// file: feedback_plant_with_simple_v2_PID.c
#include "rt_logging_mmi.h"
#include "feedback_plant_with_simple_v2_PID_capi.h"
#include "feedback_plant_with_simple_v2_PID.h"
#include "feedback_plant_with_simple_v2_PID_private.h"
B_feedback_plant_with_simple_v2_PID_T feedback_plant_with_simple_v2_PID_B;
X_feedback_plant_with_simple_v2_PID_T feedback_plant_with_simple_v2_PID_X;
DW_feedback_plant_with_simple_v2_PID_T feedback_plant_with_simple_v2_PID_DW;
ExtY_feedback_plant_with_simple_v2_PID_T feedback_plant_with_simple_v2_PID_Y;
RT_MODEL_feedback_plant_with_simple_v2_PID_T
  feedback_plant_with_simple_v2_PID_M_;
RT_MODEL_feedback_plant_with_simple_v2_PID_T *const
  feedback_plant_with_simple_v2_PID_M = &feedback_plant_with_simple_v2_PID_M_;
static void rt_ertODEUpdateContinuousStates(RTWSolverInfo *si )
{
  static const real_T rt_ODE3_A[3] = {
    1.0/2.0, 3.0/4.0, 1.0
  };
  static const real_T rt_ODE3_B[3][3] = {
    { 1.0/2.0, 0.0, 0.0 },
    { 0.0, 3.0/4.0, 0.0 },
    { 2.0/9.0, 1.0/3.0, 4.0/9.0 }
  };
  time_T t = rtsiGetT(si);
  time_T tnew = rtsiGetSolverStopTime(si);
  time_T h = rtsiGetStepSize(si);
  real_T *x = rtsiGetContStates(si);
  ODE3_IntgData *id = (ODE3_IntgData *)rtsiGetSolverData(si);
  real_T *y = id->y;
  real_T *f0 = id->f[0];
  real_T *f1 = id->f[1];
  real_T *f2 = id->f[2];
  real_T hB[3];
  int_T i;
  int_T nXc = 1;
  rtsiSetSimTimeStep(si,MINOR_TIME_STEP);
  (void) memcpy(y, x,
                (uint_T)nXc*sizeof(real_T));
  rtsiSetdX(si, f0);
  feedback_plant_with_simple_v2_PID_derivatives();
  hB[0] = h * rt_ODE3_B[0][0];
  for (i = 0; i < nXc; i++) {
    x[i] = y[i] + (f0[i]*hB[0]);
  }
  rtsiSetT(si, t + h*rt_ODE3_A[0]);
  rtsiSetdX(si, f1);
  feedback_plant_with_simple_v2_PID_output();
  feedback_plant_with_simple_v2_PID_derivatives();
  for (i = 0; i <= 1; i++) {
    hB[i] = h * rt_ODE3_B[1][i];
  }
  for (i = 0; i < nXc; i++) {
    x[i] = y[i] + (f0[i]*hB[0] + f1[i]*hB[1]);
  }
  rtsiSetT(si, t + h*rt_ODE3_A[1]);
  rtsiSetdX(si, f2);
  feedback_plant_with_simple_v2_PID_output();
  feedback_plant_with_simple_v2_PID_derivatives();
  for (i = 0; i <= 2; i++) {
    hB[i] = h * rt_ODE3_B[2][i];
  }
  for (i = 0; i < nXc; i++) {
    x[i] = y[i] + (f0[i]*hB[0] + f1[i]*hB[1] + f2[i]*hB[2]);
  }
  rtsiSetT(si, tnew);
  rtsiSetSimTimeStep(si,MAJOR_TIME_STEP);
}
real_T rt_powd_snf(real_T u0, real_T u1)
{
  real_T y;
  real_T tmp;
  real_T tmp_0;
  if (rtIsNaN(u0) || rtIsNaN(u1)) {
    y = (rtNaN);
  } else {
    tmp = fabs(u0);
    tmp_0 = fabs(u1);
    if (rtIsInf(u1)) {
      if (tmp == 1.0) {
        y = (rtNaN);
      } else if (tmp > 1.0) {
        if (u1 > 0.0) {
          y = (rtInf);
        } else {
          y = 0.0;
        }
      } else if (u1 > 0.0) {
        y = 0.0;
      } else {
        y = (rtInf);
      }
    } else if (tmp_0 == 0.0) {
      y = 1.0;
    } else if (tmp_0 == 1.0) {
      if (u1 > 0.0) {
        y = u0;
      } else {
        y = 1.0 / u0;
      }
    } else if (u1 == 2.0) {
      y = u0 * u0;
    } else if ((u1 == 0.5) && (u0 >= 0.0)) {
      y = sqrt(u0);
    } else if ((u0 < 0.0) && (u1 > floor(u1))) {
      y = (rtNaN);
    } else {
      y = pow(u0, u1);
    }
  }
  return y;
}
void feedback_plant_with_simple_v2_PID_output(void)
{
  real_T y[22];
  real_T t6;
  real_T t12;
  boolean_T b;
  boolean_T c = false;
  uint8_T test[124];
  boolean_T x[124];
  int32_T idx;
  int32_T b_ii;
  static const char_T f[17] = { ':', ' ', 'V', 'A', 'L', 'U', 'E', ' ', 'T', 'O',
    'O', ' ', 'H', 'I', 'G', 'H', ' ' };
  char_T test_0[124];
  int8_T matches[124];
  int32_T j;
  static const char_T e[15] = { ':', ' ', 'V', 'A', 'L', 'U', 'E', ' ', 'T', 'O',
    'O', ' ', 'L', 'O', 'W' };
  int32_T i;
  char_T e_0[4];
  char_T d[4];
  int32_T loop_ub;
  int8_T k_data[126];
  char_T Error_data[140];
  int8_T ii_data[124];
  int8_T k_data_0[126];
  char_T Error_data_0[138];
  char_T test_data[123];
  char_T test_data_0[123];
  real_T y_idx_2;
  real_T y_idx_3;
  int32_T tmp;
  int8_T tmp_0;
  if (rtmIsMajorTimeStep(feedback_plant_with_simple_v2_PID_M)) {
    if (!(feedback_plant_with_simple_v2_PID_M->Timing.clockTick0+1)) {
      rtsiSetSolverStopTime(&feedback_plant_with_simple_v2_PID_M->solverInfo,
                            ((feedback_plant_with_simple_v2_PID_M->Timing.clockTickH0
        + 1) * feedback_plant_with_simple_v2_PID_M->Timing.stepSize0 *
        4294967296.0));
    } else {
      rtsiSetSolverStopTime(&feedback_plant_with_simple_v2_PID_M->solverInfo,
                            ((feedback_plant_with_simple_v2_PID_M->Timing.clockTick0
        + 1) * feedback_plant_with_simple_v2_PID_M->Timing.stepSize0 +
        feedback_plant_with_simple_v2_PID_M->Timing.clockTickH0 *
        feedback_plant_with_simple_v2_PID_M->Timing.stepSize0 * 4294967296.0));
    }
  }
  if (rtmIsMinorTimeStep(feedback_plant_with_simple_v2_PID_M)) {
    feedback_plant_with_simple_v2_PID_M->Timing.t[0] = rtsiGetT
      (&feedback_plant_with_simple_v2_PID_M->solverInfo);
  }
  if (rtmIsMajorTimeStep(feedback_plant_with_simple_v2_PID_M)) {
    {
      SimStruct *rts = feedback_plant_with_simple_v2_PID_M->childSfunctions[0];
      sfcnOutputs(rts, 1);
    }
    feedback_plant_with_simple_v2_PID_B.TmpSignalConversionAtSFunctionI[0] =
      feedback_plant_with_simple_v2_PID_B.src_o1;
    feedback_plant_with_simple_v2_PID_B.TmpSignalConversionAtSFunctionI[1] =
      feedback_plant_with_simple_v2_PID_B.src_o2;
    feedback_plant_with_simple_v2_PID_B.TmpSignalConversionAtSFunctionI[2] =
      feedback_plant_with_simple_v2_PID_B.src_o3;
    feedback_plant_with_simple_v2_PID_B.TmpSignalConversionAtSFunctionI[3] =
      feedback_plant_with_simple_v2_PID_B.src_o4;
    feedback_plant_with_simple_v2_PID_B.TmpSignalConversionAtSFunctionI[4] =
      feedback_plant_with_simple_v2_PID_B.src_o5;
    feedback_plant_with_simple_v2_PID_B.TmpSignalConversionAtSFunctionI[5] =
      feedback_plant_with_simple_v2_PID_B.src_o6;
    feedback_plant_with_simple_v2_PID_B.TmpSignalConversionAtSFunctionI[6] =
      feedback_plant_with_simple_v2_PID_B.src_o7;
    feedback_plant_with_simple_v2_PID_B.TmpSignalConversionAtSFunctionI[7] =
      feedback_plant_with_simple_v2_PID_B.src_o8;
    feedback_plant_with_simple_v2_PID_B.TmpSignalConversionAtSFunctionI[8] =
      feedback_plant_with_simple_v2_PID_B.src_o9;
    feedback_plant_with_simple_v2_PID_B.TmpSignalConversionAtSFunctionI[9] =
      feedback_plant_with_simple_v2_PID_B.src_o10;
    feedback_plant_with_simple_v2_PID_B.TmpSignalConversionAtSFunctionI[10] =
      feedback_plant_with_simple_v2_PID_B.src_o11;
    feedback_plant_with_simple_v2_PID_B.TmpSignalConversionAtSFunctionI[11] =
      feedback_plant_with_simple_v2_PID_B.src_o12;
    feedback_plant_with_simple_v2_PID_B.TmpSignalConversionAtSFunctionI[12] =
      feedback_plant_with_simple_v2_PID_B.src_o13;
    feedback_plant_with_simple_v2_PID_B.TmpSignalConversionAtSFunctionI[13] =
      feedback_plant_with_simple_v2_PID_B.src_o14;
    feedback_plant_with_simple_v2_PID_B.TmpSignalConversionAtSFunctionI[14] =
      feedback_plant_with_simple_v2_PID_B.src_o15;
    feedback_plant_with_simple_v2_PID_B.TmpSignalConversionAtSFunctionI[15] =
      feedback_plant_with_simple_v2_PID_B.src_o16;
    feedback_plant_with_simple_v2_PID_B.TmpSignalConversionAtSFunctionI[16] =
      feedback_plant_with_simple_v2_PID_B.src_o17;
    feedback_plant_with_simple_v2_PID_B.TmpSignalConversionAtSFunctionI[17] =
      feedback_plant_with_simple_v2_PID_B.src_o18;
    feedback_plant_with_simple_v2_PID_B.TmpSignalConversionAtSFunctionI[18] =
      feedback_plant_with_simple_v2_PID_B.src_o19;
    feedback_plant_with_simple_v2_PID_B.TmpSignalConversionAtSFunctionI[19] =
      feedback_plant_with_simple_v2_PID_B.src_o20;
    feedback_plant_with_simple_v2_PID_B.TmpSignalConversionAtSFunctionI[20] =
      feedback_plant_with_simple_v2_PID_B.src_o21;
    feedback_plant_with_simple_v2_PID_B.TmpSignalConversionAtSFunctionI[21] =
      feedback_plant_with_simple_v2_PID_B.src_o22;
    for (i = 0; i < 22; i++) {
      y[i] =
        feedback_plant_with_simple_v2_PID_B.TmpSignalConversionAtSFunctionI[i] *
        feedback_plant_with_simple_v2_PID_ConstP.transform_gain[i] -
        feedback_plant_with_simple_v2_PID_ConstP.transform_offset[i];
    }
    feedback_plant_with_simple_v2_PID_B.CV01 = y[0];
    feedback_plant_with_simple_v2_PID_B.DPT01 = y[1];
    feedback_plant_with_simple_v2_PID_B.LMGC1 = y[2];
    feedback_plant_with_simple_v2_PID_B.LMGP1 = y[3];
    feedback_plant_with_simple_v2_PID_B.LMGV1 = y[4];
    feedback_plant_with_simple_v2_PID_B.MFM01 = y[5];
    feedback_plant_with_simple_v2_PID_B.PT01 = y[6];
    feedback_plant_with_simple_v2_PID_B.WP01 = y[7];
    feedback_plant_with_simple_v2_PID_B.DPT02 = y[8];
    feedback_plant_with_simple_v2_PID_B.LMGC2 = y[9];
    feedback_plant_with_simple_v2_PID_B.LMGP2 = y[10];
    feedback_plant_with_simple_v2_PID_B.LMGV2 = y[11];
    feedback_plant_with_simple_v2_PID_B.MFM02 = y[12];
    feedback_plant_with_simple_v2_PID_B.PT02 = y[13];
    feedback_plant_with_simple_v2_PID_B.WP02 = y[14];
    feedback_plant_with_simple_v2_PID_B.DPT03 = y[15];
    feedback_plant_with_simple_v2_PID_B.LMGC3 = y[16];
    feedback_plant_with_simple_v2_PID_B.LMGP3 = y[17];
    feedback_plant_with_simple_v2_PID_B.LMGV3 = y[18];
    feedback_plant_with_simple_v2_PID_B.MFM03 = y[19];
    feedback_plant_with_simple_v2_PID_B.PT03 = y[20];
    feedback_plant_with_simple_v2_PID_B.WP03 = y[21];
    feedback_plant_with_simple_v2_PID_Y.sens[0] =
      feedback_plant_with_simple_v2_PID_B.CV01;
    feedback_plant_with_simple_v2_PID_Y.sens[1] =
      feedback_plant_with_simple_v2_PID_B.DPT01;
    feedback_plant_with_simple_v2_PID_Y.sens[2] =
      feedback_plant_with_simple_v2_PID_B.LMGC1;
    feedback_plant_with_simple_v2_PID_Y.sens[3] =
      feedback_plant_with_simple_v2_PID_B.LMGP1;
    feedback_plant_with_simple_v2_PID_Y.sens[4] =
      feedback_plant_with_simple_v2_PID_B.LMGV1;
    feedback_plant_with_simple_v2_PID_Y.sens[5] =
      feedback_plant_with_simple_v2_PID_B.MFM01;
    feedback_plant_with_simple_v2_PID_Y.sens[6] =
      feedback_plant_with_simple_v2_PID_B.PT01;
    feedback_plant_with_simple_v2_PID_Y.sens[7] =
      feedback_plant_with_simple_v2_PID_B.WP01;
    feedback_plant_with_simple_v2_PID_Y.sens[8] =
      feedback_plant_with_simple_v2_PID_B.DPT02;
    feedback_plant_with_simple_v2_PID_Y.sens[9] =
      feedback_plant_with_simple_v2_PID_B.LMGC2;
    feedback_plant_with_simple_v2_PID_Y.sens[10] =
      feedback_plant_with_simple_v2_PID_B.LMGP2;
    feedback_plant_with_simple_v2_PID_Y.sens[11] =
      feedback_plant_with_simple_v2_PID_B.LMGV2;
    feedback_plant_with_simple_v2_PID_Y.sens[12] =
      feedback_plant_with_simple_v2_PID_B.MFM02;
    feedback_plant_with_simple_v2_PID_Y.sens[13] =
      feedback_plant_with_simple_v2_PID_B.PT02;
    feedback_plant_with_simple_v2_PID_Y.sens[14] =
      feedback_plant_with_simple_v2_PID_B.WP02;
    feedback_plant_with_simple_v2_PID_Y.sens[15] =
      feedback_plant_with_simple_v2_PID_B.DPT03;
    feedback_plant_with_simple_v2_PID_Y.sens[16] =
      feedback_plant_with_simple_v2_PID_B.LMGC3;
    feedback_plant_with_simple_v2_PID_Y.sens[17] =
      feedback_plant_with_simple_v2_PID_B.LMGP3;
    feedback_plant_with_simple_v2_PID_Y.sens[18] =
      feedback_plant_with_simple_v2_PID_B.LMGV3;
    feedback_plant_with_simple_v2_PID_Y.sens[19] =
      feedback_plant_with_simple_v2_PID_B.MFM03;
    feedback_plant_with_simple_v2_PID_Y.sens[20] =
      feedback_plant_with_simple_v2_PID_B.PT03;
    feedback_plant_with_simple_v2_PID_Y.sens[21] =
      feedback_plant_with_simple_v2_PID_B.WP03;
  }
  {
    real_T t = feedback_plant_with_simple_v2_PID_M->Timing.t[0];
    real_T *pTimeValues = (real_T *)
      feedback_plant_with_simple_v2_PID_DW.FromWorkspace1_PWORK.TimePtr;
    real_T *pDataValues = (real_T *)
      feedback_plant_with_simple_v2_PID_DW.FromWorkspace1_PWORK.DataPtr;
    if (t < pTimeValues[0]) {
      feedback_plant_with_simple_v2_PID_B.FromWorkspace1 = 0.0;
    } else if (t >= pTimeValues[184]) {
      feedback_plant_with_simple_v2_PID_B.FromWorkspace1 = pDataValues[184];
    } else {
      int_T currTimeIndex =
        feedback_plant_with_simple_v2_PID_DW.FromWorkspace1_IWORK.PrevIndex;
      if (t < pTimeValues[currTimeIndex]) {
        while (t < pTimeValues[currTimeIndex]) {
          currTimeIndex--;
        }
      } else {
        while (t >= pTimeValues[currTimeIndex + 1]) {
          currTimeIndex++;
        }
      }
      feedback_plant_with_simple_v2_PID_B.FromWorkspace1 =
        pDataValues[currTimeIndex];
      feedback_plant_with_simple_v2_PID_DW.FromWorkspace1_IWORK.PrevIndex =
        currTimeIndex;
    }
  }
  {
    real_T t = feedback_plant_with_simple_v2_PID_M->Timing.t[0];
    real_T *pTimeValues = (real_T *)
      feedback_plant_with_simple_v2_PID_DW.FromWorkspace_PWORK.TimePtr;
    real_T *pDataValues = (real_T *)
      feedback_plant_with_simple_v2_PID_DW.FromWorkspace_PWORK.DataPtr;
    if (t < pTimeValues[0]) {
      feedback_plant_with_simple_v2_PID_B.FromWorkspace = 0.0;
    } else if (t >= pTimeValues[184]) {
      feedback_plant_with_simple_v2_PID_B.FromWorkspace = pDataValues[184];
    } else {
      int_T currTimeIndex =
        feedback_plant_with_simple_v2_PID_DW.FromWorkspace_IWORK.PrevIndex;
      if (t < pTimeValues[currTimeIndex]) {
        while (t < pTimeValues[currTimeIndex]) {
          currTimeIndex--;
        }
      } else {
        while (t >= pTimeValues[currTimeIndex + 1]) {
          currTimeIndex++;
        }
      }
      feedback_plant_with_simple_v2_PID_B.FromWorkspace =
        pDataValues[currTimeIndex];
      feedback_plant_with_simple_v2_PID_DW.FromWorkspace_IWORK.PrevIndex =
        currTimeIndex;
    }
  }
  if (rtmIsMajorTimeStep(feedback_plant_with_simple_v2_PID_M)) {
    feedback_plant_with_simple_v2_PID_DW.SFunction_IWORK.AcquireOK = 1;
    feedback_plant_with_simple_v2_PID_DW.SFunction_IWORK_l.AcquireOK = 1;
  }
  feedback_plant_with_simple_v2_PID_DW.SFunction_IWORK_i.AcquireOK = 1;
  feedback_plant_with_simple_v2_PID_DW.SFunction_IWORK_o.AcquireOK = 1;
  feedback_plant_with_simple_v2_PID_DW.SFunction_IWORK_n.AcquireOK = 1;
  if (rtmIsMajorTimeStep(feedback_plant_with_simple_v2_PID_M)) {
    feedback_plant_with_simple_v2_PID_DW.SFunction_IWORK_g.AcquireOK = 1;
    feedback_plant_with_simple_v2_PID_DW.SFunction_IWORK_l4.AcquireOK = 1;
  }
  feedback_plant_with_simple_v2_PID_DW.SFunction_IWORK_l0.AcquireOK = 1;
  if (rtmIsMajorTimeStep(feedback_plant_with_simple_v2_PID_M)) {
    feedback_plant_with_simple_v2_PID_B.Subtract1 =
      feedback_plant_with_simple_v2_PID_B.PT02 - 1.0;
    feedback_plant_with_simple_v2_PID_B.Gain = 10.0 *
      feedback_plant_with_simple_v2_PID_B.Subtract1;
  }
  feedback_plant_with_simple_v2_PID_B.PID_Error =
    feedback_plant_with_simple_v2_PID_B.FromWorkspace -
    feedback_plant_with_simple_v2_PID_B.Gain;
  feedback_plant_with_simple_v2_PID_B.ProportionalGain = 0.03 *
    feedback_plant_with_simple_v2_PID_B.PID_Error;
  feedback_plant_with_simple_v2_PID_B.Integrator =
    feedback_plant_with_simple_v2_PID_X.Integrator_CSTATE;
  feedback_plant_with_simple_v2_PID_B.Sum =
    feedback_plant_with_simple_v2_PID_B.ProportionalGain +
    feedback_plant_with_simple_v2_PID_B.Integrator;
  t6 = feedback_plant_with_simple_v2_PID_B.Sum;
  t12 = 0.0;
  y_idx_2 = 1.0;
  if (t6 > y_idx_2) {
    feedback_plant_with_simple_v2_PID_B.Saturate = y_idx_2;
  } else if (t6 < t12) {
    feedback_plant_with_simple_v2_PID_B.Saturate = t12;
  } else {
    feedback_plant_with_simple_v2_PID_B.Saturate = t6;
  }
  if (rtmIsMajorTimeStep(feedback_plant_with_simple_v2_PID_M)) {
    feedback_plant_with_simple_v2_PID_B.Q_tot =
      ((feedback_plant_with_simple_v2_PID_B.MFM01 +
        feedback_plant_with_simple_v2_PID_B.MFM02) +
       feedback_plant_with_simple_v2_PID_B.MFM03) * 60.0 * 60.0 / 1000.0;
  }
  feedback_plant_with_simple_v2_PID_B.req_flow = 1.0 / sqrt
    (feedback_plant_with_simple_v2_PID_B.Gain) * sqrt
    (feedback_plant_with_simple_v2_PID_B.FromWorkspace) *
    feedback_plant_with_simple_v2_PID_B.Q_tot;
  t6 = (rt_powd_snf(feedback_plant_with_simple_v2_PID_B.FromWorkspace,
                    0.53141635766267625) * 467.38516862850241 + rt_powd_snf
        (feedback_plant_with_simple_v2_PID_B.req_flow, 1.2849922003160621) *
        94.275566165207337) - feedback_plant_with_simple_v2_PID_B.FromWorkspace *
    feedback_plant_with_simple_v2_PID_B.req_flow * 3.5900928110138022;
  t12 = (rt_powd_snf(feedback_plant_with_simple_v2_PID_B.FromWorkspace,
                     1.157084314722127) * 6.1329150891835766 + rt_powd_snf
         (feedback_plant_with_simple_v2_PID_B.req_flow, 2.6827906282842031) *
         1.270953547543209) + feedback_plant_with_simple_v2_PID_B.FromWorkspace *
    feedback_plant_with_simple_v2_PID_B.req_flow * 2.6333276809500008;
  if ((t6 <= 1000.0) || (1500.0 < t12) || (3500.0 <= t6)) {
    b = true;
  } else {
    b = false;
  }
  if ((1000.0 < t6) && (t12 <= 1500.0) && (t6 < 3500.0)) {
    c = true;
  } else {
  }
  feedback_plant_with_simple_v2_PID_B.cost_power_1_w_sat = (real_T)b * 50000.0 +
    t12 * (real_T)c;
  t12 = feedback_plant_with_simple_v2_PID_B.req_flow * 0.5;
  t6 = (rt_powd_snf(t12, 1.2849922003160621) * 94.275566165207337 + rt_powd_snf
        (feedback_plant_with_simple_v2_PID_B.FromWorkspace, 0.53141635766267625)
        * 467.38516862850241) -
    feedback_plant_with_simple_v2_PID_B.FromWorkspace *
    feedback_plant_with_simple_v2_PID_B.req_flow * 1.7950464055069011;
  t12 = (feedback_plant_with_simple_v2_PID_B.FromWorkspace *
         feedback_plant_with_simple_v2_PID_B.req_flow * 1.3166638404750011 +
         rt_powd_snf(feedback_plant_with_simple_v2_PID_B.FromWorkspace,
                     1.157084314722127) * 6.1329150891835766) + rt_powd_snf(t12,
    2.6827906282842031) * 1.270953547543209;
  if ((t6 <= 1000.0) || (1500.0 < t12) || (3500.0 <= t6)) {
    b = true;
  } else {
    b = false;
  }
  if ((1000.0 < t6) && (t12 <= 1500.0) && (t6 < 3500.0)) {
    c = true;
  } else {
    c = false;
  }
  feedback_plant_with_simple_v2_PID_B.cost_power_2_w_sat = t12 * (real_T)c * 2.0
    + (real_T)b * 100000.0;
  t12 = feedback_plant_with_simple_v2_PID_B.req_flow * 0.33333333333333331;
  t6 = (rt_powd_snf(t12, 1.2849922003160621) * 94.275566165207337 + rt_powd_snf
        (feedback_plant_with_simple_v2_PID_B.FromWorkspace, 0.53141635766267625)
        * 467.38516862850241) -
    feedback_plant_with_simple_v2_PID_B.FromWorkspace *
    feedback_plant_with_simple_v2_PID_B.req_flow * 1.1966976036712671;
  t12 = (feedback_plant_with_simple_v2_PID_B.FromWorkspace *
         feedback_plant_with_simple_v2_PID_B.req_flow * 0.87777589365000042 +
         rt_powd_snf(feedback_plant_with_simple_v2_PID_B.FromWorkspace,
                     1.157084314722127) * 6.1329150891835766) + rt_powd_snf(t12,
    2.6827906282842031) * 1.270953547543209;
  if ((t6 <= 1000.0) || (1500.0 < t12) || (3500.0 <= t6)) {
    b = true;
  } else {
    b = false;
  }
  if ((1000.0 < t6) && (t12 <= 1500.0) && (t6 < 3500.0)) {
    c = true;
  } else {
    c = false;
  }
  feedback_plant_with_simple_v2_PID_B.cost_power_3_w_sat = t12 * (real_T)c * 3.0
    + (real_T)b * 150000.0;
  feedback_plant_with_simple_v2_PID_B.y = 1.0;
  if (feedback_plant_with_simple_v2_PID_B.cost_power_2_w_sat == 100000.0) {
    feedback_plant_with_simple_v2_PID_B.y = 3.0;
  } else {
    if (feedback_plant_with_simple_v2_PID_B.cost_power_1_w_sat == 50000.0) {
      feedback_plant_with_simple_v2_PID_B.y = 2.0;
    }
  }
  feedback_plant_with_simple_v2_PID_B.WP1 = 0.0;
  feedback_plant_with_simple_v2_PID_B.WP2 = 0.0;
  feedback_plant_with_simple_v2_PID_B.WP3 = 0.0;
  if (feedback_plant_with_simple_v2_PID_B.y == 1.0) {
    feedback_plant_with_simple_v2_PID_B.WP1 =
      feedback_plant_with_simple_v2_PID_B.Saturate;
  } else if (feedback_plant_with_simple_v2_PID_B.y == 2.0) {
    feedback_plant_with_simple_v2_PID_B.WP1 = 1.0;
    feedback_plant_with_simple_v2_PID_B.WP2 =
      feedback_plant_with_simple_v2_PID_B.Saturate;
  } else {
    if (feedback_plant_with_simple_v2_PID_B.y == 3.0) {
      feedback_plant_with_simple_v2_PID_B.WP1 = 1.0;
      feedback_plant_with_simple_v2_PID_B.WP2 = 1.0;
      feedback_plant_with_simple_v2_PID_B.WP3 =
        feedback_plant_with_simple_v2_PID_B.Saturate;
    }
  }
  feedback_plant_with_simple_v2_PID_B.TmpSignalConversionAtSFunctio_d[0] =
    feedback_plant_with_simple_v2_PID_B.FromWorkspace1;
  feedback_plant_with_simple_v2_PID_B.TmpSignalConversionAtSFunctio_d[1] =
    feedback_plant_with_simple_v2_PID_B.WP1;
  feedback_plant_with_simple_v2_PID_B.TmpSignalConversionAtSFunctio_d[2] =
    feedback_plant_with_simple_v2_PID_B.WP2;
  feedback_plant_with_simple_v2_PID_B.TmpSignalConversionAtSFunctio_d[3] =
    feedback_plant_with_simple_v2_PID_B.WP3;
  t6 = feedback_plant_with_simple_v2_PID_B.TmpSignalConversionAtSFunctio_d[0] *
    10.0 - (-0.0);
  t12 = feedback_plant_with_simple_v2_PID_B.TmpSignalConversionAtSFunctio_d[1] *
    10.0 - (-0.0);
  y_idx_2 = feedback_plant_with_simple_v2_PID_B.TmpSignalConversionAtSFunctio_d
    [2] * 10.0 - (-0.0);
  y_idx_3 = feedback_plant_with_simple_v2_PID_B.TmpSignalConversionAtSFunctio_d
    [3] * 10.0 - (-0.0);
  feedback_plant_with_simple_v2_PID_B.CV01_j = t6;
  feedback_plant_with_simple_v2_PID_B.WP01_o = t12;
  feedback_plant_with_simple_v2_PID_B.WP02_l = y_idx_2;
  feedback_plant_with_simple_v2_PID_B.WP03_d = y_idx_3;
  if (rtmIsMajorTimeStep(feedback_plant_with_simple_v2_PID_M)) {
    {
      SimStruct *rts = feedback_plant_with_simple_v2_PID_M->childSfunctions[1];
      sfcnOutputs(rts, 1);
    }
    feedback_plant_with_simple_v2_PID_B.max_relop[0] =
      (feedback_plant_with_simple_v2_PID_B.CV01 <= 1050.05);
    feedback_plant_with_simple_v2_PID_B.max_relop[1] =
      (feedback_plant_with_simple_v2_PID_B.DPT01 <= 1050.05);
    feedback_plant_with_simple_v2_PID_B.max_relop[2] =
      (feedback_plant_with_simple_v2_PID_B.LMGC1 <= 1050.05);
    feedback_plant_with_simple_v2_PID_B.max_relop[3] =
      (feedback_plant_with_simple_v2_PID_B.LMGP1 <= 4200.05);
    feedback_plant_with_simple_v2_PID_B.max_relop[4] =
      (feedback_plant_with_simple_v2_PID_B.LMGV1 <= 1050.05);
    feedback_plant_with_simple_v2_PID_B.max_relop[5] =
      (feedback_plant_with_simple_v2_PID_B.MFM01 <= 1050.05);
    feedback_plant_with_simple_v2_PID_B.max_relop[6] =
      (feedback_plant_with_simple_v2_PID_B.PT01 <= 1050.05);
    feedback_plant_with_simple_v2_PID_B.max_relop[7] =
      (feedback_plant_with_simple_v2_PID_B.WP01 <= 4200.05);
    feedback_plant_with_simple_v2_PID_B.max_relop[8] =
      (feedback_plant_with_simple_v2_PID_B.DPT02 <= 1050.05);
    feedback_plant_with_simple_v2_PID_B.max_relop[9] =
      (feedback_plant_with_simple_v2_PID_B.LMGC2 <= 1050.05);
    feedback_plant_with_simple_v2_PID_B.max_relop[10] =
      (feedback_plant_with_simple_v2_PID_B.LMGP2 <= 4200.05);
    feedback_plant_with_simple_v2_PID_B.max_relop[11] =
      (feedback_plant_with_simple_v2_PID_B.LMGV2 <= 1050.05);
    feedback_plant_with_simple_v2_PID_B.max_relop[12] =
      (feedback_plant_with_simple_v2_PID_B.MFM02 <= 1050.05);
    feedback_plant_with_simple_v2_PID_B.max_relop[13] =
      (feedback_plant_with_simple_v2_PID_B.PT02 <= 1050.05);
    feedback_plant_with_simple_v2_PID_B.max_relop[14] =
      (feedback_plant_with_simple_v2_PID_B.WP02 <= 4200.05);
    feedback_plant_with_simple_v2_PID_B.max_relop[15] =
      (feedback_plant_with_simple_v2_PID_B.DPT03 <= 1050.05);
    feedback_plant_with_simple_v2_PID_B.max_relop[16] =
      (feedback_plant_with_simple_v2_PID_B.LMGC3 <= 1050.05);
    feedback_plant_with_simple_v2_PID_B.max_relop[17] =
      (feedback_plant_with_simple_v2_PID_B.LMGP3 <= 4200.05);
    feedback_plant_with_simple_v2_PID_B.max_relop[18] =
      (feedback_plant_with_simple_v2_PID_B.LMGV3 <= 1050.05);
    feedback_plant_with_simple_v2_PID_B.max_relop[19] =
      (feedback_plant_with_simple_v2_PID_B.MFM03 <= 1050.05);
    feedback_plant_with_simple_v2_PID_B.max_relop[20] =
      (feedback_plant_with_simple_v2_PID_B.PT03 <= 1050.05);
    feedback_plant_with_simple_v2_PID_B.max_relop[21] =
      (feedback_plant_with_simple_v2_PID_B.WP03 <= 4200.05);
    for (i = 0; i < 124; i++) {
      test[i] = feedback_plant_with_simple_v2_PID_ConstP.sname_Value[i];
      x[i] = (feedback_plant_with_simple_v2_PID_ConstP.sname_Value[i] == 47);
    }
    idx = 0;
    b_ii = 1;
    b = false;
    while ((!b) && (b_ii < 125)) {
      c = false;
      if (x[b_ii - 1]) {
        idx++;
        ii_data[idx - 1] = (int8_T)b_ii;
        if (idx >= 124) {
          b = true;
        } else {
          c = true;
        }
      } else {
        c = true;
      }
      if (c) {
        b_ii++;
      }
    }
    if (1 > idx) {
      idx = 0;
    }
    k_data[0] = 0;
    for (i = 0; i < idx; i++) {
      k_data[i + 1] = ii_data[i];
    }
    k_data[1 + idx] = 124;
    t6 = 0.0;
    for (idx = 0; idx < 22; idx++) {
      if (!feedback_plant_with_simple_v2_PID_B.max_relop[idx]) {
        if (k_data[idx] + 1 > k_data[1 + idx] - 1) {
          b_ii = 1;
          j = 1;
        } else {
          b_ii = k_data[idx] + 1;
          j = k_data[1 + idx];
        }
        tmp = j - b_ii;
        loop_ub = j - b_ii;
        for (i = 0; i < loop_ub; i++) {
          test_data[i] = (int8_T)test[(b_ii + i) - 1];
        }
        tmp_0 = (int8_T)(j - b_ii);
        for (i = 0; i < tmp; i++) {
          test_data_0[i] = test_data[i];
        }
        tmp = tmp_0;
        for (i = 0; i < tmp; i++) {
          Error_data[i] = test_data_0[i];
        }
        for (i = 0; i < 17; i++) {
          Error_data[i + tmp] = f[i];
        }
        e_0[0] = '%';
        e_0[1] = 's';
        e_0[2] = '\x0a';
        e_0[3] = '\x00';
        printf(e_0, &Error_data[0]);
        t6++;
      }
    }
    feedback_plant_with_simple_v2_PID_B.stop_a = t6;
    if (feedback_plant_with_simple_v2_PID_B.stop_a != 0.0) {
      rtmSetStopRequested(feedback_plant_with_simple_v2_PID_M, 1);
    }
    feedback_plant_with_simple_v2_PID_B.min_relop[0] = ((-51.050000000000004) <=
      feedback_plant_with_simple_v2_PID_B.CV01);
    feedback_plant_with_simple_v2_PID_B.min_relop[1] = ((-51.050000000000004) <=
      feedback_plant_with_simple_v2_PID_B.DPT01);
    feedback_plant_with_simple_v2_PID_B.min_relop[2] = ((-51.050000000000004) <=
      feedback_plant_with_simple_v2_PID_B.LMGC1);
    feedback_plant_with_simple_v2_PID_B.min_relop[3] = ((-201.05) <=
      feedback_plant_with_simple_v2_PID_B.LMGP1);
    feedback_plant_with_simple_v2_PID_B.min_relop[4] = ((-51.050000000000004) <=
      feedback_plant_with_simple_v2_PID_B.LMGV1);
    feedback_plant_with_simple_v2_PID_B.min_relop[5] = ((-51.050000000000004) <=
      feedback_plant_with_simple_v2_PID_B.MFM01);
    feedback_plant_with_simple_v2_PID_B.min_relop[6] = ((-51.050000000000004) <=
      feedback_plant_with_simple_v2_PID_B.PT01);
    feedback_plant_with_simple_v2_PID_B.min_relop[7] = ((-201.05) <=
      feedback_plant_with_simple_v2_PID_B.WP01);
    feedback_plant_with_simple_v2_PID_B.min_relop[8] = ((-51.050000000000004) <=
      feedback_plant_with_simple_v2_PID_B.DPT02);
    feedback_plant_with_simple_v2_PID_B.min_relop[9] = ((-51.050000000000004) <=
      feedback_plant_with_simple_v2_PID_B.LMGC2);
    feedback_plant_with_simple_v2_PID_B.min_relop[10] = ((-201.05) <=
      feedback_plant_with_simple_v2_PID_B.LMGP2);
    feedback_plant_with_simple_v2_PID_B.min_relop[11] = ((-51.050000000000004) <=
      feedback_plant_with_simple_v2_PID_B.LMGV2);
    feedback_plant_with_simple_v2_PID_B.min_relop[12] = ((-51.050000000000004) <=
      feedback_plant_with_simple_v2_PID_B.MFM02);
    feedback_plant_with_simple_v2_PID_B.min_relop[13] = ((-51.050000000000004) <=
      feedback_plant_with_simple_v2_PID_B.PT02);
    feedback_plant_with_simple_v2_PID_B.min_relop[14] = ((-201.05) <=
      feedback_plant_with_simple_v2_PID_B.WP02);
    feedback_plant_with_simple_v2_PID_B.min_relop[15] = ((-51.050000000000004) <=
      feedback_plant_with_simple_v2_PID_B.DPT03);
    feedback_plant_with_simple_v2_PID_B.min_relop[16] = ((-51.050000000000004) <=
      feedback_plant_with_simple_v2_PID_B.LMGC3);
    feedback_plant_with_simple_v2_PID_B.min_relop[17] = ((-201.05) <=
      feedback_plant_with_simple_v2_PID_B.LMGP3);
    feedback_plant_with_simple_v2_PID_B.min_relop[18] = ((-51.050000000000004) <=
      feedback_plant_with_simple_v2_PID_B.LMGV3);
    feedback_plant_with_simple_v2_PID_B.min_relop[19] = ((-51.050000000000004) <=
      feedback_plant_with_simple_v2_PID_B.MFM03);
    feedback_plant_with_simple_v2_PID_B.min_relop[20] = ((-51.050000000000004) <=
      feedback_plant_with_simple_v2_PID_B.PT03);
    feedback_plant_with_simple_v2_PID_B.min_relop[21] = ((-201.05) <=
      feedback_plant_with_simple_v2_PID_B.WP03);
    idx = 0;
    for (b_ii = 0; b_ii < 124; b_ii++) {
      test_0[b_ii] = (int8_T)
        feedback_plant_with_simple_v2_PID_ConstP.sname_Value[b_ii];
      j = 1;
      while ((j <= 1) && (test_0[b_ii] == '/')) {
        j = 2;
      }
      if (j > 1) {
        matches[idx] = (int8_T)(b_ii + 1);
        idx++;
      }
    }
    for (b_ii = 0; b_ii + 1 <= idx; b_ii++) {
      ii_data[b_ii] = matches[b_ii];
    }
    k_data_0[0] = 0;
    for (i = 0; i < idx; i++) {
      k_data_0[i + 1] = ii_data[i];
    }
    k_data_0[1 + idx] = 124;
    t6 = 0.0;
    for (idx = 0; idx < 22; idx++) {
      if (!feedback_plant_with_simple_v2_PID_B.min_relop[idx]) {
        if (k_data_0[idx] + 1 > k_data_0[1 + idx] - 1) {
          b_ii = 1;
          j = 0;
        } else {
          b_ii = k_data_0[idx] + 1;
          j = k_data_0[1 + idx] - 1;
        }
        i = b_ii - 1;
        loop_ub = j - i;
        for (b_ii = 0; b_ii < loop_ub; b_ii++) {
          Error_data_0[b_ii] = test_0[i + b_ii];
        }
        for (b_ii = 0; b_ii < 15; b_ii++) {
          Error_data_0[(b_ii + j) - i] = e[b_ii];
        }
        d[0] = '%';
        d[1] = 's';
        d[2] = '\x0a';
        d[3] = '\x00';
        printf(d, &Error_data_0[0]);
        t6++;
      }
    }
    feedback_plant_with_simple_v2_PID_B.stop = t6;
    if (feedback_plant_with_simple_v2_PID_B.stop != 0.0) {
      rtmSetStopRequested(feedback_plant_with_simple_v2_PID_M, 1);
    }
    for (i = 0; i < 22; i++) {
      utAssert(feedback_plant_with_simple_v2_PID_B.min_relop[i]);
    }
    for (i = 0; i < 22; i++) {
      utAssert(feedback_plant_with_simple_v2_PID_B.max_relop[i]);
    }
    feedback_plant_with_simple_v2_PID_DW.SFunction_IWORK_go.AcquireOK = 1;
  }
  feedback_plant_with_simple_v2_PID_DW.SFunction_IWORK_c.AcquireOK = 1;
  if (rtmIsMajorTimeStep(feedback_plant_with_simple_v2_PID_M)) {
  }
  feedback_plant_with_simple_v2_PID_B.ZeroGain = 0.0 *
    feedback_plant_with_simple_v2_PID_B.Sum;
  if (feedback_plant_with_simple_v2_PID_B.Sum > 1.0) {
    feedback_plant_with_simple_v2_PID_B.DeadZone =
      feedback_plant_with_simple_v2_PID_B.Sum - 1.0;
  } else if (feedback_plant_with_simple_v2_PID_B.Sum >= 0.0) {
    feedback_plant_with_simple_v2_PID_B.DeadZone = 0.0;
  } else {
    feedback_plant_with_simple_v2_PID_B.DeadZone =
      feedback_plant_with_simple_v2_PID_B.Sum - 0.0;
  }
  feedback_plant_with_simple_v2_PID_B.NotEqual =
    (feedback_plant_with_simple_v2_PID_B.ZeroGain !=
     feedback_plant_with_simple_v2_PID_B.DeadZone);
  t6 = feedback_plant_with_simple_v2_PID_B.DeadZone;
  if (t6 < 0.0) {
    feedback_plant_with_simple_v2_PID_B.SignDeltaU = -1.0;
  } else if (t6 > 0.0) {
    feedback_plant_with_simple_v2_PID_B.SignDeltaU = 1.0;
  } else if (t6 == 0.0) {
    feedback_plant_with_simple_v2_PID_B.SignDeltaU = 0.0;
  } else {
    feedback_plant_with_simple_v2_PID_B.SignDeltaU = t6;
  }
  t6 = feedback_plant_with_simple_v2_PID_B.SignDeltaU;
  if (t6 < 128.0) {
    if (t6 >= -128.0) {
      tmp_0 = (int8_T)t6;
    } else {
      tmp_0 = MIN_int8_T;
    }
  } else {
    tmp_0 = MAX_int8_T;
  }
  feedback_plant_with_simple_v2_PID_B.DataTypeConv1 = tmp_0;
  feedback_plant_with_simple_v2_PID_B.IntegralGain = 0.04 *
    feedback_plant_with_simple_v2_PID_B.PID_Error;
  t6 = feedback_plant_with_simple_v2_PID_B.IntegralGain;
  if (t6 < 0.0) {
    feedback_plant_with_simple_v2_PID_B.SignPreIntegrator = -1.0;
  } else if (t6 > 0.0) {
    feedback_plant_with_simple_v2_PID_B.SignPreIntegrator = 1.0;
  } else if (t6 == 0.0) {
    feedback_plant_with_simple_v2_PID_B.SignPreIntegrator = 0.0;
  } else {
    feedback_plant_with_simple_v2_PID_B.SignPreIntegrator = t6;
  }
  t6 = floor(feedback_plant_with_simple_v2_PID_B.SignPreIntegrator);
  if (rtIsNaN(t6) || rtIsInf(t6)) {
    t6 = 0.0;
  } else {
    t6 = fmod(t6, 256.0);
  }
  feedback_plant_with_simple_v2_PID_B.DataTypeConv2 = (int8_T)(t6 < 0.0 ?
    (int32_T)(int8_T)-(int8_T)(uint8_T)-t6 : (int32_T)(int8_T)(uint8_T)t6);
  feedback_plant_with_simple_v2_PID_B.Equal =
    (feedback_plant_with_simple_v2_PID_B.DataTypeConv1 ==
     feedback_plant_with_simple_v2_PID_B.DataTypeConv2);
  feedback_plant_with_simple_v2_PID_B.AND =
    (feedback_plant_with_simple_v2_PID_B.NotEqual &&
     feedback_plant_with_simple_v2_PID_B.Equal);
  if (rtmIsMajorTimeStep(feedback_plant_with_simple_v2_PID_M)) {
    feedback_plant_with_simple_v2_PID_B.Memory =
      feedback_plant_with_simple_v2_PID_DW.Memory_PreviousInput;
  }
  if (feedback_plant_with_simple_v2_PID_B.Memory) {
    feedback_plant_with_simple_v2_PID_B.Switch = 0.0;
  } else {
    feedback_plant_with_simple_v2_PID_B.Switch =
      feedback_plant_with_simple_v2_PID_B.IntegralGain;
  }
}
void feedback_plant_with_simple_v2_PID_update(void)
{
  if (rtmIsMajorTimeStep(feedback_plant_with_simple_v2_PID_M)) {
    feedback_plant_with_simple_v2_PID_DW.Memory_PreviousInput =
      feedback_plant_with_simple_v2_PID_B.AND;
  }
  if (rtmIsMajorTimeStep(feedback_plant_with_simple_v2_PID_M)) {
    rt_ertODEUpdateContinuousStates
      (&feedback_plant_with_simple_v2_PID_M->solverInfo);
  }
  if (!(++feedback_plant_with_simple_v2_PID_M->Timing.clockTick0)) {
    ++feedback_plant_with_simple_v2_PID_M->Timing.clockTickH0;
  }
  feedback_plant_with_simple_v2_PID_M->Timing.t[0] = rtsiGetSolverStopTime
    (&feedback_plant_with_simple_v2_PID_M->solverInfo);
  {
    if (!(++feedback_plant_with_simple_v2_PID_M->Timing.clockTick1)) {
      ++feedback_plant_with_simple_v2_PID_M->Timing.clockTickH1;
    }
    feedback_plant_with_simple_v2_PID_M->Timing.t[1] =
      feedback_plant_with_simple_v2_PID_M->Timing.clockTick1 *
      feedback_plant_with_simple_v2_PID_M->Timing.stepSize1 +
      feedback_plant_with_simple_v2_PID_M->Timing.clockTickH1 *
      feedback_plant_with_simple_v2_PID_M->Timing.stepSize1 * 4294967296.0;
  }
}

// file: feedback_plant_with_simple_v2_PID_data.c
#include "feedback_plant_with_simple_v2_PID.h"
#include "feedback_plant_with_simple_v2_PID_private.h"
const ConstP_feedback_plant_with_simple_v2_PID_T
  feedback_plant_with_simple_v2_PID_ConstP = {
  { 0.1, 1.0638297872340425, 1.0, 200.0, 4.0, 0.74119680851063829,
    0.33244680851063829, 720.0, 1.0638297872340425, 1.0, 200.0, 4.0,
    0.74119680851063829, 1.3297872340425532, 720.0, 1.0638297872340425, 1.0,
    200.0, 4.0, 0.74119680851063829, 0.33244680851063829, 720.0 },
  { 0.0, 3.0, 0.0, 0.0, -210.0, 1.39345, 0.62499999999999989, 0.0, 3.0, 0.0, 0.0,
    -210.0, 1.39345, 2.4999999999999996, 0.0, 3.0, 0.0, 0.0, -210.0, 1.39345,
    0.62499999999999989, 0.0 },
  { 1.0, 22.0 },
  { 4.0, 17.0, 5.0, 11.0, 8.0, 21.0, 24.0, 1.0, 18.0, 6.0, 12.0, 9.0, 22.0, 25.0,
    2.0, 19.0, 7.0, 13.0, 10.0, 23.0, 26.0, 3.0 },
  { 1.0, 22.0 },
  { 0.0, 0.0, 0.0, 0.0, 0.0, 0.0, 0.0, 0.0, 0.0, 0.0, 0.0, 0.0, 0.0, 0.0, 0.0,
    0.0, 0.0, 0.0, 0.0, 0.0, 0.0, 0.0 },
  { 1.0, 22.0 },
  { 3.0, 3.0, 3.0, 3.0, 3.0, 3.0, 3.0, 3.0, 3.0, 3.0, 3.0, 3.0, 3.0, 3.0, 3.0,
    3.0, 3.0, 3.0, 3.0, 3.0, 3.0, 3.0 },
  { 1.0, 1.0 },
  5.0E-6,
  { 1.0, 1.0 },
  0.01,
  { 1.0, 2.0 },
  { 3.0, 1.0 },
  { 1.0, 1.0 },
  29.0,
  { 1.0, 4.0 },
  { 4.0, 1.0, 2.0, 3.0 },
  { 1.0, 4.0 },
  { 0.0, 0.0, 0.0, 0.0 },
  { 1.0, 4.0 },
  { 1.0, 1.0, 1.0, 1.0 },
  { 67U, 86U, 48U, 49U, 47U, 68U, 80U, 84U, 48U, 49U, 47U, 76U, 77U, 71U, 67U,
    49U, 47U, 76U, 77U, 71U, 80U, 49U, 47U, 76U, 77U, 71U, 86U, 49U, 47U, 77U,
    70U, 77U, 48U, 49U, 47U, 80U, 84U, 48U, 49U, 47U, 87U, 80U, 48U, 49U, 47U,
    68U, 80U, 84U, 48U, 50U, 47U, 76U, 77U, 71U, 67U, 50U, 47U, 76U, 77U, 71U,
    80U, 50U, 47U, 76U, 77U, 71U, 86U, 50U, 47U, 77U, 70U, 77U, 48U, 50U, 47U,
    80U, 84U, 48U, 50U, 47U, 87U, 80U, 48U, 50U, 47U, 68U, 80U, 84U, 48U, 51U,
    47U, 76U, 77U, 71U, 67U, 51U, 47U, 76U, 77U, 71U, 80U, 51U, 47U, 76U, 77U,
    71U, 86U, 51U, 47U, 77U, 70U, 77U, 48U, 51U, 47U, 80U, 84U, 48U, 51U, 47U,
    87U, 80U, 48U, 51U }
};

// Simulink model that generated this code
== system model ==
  sens : Outport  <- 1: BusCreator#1
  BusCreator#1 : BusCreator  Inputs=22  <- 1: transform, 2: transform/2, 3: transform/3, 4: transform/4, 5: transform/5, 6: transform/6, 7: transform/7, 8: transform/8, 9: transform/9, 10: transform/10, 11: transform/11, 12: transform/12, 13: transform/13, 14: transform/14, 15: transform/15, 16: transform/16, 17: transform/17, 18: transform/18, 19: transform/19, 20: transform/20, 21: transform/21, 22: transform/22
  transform : MATLAB Function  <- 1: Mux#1
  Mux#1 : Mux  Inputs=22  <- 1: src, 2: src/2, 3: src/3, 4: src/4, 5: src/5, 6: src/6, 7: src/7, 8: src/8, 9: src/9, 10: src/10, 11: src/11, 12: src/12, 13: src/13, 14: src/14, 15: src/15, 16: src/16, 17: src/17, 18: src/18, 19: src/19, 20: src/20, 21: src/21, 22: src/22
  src : xpcnilib/A//D/M Series/PCI-6229 AD
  PCI6229DA#1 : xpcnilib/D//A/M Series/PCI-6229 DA  <- 1: MATLABFunction#1, 2: MATLABFunction#1/2, 3: MATLABFunction#1/3, 4: MATLABFunction#1/4
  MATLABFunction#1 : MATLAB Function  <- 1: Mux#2, 2: gain, 3: offset
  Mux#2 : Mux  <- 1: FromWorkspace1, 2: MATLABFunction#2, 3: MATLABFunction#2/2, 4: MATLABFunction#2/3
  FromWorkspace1 : FromWorkspace
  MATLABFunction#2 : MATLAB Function  <- 1: PIDController#1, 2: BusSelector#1
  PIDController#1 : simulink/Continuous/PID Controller  Controller=PI  TimeDomain=Continuous-time  IntegratorMethod=Forward Euler  Form=Parallel  P=0.03  I=0.04  D=0  N=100  InitialConditionForIntegrator=0  ExternalReset=none  LimitOutput=on  UpperSaturationLimit=1  LowerSaturationLimit=0  <- 1: Sum
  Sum : Sum  Inputs=+-  <- 1: FromWorkspace, 2: Gain
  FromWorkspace : FromWorkspace
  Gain : Gain  Gain=10  <- 1: Subtract1
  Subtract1 : Sum  Inputs=+-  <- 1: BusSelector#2, 2: Constant#1
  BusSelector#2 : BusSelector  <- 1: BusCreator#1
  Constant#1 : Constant
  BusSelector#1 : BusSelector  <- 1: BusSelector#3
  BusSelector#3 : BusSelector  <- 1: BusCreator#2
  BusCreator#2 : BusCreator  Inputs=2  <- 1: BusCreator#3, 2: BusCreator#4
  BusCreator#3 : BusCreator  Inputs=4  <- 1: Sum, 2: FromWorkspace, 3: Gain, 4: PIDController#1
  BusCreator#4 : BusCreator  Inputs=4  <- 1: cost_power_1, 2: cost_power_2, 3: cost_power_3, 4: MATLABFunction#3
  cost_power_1 : MATLAB Function  <- 1: FromWorkspace, 2: MATLABFunction#4
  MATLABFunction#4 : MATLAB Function  <- 1: Gain, 2: FromWorkspace, 3: MATLABFunction#5
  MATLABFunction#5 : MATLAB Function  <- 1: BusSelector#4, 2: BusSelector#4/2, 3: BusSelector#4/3
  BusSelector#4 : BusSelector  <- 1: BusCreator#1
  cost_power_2 : MATLAB Function  <- 1: FromWorkspace, 2: MATLABFunction#4
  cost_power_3 : MATLAB Function  <- 1: FromWorkspace, 2: MATLABFunction#4
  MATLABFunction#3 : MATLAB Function  <- 1: cost_power_1, 2: cost_power_2, 3: cost_power_3
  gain : Constant  Value=gain
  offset : Constant  Value=offset
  stop : Stop  <- 1: MATLABFunction#6
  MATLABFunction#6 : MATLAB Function  <- 1: CheckStaticUpperBound#1, 2: sname
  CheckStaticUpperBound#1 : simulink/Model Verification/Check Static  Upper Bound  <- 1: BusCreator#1
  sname : Constant  Value=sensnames
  Stop#1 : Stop  <- 1: MATLABFunction#7
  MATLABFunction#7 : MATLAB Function  <- 1: CheckStaticLowerBound#1, 2: sname
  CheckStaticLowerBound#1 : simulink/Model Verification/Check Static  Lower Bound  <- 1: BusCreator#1
== matlab function transform ==
function [CV01,WP01,WP02,WP03]  = fcn(u,gain,offset)
   y = u.*gain-offset;
CV01 = y(1);
WP01 = y(2);
WP02 = y(3);
WP03 = y(4);

== matlab function transform ==
function [CV01,DPT01,LMGC1,LMGP1,LMGV1,MFM01,PT01,WP01,DPT02,LMGC2,LMGP2,LMGV2,MFM02,PT02,WP02,DPT03,LMGC3,LMGP3,LMGV3,MFM03,PT03,WP03]  = fcn(u,gain,offset)
   y = u(:).*gain(:)-offset(:);
CV01 = y(1);
DPT01 = y(2);
LMGC1 = y(3);
LMGP1 = y(4);
LMGV1 = y(5);
MFM01 = y(6);
PT01 = y(7);
WP01 = y(8);
DPT02 = y(9);
LMGC2 = y(10);
LMGP2 = y(11);
LMGV2 = y(12);
MFM02 = y(13);
PT02 = y(14);
WP02 = y(15);
DPT03 = y(16);
LMGC3 = y(17);
LMGP3 = y(18);
LMGV3 = y(19);
MFM03 = y(20);
PT03 = y(21);
WP03 = y(22);

== matlab function MATLAB Function ==
function Q_tot = fcn(Q1, Q2, Q3)

Q_tot = ((Q1 + Q2 + Q3) *60 * 60)/1000;

== matlab function MATLABFunction#2 ==
function [WP1, WP2, WP3] = fcn(pump_speed, Numbers_of_Pumps)
WP1 = 0;
WP2 = 0;
WP3 = 0;
if Numbers_of_Pumps == 1
    WP1 = pump_speed;
elseif Numbers_of_Pumps == 2
    WP1 = 1;
    WP2 = pump_speed;
elseif Numbers_of_Pumps == 3
    WP1 = 1;
    WP2 = 1;
    WP3 = pump_speed;
end

== matlab function MATLAB Function ==
 function y = fcn(p1, p2, p3)
y = 1;
if p2 == 100000
    %2 pumps?
    y = 3;
elseif p1 == 50000
    y = 2;
    %3 pumps? 
end

== matlab function cost_power_1 ==
function cost_power_1_w_sat = cost_power_1(H,Q)
%#codegen

%    This function was generated by the Symbolic Math Toolbox version 7.0.
%    22-Aug-2016 11:17:26

t2 = H.^5.314163576626763e-1;
t3 = t2.*4.673851686285024e2;
t4 = Q.^1.284992200316062;
t5 = t4.*9.427556616520734e1;
t13 = H.*Q.*3.590092811013802;
t6 = t3+t5-t13;
t7 = H.^1.157084314722127;
t8 = t7.*6.132915089183577;
t9 = Q.^2.682790628284203;
t10 = t9.*1.270953547543209;
t11 = H.*Q.*2.633327680950001;
t12 = t8+t10+t11;
cost_power_1_w_sat = double(((t6 <= 1.0e3) || (1.5e3 < t12)) || (3.5e3 <= t6)).*5.0e4+t12.*double(((1.0e3 < t6) && (t12 <= 1.5e3)) && (t6 < 3.5e3));

== matlab function cost_power_2 ==
function cost_power_2_w_sat = cost_power_2(H,Q)
%#codegen

%    This function was generated by the Symbolic Math Toolbox version 7.0.
%    22-Aug-2016 11:17:26

t2 = Q.*(1.0./2.0);
t3 = t2.^1.284992200316062;
t4 = t3.*9.427556616520734e1;
t5 = H.^5.314163576626763e-1;
t6 = t5.*4.673851686285024e2;
t14 = H.*Q.*1.795046405506901;
t7 = t4+t6-t14;
t8 = H.^1.157084314722127;
t9 = t8.*6.132915089183577;
t10 = H.*Q.*1.316663840475001;
t11 = t2.^2.682790628284203;
t12 = t11.*1.270953547543209;
t13 = t9+t10+t12;
cost_power_2_w_sat = double(((t7 <= 1.0e3) || (1.5e3 < t13)) || (3.5e3 <= t7)).*1.0e5+t13.*double(((1.0e3 < t7) && (t13 <= 1.5e3)) && (t7 < 3.5e3)).*2.0;

== matlab function cost_power_3 ==
function cost_power_3_w_sat = cost_power_3(H,Q)
%#codegen

%    This function was generated by the Symbolic Math Toolbox version 7.0.
%    22-Aug-2016 11:17:26

t2 = Q.*(1.0./3.0);
t3 = t2.^1.284992200316062;
t4 = t3.*9.427556616520734e1;
t5 = H.^5.314163576626763e-1;
t6 = t5.*4.673851686285024e2;
t14 = H.*Q.*1.196697603671267;
t7 = t4+t6-t14;
t8 = H.^1.157084314722127;
t9 = t8.*6.132915089183577;
t10 = H.*Q.*8.777758936500004e-1;
t11 = t2.^2.682790628284203;
t12 = t11.*1.270953547543209;
t13 = t9+t10+t12;
cost_power_3_w_sat = double(((t7 <= 1.0e3) || (1.5e3 < t13)) || (3.5e3 <= t7)).*1.5e5+t13.*double(((1.0e3 < t7) && (t13 <= 1.5e3)) && (t7 < 3.5e3)).*3.0;

== matlab function MATLABFunction#4 ==
function req_flow = valve_CV_esti_Test(H_current,H_ref,Q_current)
%#codegen

%    This function was generated by the Symbolic Math Toolbox version 7.0.
%    22-Aug-2016 11:17:28

req_flow = 1.0./sqrt(H_current).*sqrt(H_ref).*Q_current;

== matlab function MATLABFunction#6 ==
function stop  = fcn(chk, sensnames)
%#codegen
%test = char(sensnames.');
test = sensnames.';
k = find(test == 47);
k = [0 k];
k = [k numel(test)];
stop = 0;
for i = 1:numel(chk)
    if chk(i) == 0
        str = char(test(k(i)+1:k(i+1)-1));
        Error = [str ': VALUE TOO HIGH ']
        coder.ceval('printf', ['%s' 10 0], Error);
        stop = stop+1;
    end
end

== matlab function MATLABFunction#7 ==
function stop  = fcn(chk, sensnames)
%#codegen
test = char(sensnames.');
k = strfind(test, '/');
k = [0 k];
k = [k numel(sensnames)];
stop = 0;
for i = 1:numel(chk)
    if chk(i) == 0
        str = char(test(k(i)+1:k(i+1)-1));
        Error = [str ': VALUE TOO LOW']
        coder.ceval('printf', ['%s' 10 0], Error);
        stop = stop+1;
    end
end
